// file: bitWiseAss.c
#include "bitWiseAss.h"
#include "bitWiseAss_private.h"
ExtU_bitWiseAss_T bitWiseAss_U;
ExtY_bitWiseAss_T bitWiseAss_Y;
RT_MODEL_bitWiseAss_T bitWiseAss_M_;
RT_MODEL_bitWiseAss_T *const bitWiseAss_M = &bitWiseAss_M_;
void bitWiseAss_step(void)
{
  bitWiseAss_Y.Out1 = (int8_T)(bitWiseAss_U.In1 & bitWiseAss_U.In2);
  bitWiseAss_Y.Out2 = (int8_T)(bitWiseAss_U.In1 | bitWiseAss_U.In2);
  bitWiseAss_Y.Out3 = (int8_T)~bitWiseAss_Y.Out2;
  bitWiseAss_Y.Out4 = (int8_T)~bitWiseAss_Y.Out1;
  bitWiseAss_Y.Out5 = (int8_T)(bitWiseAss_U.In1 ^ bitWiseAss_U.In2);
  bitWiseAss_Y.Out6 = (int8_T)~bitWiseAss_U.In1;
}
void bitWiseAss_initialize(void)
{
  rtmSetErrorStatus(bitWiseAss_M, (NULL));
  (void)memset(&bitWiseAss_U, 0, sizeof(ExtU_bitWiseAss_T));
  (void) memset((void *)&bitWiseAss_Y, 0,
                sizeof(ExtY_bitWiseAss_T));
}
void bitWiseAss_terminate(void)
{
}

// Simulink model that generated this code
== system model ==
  In1 : Inport
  In2 : Inport
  Out1 : Outport  <- 1: BitwiseOperator#1
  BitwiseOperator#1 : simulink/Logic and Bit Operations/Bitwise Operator  logicop=AND  BitMask=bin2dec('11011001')  <- 1: In1, 2: In2
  Out2 : Outport  <- 1: BitwiseOperator#2
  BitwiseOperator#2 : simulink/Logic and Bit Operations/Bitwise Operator  logicop=OR  BitMask=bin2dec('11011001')  <- 1: In1, 2: In2
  Out3 : Outport  <- 1: BitwiseOperator#3
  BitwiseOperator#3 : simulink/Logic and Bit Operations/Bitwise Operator  logicop=NOR  BitMask=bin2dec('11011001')  <- 1: In1, 2: In2
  Out4 : Outport  <- 1: BitwiseOperator#4
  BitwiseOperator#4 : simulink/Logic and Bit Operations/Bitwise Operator  logicop=NAND  BitMask=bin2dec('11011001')  <- 1: In1, 2: In2
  Out5 : Outport  <- 1: BitwiseOperator#5
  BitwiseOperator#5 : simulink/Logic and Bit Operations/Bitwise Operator  logicop=XOR  BitMask=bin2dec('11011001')  <- 1: In1, 2: In2
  Out6 : Outport  <- 1: BitwiseOperator#6
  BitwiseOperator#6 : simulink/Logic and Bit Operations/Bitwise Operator  logicop=NOT  BitMask=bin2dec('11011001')  <- 1: In1
